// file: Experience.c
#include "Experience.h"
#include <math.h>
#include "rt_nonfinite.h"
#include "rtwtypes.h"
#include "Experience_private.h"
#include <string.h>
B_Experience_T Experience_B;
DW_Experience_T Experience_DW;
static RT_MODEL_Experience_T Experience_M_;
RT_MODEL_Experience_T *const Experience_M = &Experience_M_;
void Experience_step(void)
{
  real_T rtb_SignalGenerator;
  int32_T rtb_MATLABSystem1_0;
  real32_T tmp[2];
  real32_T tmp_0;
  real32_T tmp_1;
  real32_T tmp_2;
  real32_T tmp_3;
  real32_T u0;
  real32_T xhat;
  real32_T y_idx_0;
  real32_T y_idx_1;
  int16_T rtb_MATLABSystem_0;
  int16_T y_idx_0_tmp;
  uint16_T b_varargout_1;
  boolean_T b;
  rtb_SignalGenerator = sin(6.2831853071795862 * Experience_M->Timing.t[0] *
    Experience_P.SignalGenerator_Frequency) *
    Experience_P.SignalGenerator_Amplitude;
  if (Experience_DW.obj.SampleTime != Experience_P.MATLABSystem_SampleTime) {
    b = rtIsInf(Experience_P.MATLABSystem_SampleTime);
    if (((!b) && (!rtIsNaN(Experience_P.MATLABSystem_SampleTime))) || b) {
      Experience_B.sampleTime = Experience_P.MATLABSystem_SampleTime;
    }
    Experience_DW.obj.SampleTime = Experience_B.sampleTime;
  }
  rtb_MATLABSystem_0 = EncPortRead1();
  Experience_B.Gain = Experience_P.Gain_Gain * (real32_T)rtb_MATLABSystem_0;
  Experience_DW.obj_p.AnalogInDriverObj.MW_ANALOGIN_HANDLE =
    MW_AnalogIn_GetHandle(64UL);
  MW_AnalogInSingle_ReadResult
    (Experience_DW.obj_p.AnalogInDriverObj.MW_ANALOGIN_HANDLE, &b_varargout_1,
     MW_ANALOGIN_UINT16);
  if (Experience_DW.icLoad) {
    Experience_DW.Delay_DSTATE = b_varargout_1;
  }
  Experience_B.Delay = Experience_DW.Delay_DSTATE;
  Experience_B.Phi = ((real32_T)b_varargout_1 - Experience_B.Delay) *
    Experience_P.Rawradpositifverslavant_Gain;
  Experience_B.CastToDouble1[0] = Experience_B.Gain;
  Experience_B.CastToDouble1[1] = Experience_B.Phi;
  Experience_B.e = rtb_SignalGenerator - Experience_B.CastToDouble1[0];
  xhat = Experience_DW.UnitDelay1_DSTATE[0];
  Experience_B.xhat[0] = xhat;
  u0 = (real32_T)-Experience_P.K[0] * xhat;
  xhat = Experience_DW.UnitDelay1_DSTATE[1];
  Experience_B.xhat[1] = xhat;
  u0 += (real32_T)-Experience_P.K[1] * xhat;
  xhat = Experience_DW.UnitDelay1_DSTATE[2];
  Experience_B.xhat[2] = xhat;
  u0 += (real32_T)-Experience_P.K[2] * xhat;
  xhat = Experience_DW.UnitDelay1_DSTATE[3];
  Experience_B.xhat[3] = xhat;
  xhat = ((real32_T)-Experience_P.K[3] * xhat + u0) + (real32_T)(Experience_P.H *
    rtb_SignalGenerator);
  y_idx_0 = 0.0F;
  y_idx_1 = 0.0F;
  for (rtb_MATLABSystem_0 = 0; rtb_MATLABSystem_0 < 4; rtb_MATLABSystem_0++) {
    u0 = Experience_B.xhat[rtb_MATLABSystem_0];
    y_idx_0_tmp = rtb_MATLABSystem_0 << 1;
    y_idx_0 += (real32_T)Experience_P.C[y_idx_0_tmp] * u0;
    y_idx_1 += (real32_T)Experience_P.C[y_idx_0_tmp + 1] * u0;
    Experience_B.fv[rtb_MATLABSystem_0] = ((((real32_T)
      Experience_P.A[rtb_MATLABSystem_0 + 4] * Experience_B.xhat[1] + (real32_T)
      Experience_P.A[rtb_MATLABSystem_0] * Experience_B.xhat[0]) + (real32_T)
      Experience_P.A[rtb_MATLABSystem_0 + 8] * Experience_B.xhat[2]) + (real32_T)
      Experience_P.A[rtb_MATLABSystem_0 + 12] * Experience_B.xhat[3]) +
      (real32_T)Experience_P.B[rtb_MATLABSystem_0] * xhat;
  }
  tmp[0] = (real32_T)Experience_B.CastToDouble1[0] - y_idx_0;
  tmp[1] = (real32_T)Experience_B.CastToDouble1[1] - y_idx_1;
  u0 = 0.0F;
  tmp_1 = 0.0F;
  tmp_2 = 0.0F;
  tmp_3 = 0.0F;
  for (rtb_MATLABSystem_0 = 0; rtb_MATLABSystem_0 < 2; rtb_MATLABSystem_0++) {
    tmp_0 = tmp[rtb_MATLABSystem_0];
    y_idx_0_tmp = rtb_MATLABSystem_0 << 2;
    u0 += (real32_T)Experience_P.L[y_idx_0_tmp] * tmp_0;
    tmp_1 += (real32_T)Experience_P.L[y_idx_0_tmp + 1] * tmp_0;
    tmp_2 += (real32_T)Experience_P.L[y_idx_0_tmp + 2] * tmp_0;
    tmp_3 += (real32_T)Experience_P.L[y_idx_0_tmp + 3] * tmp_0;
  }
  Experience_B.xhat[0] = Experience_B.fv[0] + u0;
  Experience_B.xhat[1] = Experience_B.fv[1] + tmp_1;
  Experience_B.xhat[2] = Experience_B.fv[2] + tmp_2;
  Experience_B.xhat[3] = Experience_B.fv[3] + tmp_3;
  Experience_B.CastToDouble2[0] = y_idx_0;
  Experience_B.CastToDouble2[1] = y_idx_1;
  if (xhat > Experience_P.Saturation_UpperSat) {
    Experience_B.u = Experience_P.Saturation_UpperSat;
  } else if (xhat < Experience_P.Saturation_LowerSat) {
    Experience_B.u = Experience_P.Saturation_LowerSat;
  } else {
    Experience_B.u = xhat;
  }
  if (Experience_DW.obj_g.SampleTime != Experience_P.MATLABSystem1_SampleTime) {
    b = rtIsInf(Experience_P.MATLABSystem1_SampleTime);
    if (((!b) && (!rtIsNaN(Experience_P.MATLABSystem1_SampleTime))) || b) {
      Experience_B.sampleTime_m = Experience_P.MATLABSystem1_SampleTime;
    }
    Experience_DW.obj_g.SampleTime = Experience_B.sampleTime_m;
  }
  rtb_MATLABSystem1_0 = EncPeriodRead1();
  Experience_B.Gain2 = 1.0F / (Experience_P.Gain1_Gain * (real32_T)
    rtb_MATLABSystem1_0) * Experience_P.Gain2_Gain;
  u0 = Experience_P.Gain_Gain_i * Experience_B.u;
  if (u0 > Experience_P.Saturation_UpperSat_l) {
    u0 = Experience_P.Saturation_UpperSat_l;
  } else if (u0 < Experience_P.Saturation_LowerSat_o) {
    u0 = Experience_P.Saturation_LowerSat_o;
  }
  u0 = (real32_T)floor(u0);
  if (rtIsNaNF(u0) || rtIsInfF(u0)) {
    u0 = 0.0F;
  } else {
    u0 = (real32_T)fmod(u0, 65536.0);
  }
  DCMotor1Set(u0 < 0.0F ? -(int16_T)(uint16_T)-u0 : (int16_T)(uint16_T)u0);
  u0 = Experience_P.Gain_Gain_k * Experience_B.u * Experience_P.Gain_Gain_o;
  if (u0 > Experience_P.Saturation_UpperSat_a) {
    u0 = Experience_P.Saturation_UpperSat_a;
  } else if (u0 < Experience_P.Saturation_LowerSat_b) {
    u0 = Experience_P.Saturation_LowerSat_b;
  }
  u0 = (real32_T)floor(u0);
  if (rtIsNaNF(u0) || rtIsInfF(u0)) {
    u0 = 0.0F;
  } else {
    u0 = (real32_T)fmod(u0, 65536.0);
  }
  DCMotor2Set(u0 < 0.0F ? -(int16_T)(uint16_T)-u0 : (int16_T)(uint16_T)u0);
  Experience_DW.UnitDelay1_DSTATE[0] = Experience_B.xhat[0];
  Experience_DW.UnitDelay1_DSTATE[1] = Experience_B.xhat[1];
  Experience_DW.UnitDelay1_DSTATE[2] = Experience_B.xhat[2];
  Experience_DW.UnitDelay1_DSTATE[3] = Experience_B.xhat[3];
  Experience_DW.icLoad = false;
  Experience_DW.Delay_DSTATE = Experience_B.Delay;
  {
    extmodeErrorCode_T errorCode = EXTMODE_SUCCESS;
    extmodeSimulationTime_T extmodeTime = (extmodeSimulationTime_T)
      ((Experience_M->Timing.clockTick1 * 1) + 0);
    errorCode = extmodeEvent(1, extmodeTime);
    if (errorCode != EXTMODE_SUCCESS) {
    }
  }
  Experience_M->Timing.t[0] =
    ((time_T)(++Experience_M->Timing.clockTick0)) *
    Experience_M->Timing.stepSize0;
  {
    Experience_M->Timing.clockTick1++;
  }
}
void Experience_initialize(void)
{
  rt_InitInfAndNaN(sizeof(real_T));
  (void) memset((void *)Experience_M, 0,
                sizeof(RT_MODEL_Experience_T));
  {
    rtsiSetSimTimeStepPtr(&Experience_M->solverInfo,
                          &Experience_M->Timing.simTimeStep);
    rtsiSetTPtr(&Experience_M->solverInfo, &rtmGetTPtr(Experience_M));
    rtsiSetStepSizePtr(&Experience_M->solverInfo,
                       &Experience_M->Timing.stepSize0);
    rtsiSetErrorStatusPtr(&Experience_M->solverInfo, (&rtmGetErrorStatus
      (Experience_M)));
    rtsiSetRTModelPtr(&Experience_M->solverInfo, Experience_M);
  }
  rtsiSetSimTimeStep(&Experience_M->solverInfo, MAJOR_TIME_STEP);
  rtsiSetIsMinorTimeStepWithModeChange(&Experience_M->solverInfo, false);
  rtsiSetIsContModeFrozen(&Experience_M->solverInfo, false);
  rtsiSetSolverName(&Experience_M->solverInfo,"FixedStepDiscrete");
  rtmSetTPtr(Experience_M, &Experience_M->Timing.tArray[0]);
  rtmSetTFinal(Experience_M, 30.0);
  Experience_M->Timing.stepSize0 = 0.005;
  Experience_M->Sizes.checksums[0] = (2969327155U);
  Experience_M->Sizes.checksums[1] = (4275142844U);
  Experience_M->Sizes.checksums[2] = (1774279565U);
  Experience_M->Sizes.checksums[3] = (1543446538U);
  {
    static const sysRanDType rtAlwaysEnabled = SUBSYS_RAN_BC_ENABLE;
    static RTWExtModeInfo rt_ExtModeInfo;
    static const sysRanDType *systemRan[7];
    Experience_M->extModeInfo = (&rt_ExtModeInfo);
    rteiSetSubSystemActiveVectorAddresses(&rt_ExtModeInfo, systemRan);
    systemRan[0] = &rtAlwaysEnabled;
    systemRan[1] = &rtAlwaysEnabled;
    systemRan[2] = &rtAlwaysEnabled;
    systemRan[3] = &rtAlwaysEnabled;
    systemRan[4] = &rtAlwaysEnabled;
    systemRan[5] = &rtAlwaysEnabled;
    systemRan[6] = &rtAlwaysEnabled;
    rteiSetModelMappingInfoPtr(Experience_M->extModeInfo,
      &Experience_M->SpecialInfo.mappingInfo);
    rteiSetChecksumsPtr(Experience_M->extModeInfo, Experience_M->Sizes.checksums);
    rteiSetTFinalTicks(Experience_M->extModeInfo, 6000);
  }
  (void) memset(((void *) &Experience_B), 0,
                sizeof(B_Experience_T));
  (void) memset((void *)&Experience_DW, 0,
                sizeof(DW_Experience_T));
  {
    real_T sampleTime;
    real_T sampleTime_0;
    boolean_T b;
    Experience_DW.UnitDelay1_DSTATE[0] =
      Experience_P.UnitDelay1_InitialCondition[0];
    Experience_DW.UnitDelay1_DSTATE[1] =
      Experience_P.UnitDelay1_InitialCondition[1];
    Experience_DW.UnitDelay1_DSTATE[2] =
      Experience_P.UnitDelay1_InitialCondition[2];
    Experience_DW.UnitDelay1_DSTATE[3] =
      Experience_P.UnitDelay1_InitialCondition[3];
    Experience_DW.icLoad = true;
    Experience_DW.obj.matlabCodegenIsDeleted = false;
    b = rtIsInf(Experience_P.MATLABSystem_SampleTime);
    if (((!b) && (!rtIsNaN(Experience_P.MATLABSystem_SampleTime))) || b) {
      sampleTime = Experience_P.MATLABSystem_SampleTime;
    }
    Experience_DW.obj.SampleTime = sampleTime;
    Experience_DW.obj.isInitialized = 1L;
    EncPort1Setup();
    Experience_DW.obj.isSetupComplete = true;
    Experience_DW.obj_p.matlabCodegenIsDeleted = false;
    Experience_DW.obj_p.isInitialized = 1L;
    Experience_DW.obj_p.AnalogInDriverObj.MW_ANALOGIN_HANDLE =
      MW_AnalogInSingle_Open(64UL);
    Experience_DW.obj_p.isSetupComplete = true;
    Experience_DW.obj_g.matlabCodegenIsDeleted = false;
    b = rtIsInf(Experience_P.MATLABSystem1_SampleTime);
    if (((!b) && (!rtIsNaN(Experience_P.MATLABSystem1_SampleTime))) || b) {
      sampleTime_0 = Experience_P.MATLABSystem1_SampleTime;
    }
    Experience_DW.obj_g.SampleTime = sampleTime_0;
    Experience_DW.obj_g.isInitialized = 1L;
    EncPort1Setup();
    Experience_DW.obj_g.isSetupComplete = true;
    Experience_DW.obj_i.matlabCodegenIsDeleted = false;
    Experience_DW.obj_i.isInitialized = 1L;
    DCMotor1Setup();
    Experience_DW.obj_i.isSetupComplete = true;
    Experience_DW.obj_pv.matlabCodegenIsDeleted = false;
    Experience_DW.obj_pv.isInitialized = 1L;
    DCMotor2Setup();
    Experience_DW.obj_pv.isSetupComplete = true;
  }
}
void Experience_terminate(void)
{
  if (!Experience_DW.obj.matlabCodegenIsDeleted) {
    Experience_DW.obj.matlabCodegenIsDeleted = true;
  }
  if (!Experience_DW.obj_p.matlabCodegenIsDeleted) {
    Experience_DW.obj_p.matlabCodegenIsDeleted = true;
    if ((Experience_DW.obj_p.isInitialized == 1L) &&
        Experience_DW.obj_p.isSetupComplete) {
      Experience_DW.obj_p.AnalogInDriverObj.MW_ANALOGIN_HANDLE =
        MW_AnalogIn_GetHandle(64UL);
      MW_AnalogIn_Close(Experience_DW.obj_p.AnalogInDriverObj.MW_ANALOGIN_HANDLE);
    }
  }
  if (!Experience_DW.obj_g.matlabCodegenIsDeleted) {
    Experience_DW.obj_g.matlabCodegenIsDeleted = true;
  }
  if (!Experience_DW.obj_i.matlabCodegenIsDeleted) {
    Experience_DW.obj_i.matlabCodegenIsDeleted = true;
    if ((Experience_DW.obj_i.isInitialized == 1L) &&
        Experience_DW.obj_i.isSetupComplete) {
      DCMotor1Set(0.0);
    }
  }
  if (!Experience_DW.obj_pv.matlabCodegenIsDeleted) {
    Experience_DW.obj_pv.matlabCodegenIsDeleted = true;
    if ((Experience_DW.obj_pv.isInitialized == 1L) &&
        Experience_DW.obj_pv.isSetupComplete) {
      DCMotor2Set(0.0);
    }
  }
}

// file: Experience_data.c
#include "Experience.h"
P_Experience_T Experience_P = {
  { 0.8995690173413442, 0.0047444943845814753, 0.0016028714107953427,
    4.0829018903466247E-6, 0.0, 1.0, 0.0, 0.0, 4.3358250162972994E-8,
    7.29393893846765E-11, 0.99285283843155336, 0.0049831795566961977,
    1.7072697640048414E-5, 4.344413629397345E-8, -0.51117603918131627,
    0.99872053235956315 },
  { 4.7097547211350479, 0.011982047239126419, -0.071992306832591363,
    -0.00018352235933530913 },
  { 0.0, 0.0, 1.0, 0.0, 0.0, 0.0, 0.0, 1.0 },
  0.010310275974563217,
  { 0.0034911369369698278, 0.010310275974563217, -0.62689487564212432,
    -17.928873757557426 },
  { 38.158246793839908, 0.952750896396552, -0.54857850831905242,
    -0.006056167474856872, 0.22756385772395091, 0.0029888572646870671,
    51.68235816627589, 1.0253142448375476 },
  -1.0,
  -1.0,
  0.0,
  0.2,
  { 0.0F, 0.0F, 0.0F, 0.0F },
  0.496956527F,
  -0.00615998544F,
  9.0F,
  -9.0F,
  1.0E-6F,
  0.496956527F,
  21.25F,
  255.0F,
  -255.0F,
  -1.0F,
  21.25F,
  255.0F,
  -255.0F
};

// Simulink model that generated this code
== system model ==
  MATLABSystem : MATLABSystem  <- 1: DataTypeConversion#1
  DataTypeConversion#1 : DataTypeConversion  <- 1: Saturation
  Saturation : Saturate  UpperLimit=255  LowerLimit=-255  <- 1: Gain
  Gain : Gain  Gain=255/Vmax  <- 1: Gain#1
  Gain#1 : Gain  Gain=-1  <- 1: Saturate#1
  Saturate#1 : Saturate  UpperLimit=9  LowerLimit=-9  <- 1: DataTypeConversion#2
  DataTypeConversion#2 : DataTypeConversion  <- 1: MATLABFunction#1/2
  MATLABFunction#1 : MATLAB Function  <- 1: UnitDelay1, 2: SignalGenerator, 3: CastToDouble1
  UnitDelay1 : UnitDelay  InitialCondition=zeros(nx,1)  <- 1: MATLABFunction#1
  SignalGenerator : SignalGenerator  Amplitude=0  Frequency=.2
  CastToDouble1 : DataTypeConversion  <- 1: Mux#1
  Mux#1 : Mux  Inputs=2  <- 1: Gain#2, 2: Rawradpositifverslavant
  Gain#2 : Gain  Gain=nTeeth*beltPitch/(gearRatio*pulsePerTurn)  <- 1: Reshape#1
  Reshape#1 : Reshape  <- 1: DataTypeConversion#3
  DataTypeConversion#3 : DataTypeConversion  <- 1: MATLABSystem#1
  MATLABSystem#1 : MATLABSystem
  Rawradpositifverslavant : Gain  Gain=-pi/2/255  <- 1: Sum#1
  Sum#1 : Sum  Inputs=+-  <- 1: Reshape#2, 2: Delay
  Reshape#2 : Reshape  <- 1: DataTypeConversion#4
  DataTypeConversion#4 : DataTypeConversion  <- 1: AnalogInput#1
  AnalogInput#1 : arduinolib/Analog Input  pinNumber=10
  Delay : Delay  DelayLength=1  <- 1: Delay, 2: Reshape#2
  CastToDouble2 : DataTypeConversion  <- 1: MATLABFunction#1/3
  MATLABSystem1 : MATLABSystem  <- 1: DataTypeConversion#5
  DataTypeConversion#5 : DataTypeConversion  <- 1: Saturate#2
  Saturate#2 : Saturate  UpperLimit=255  LowerLimit=-255  <- 1: Gain#3
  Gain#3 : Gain  Gain=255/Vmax  <- 1: Saturate#1
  Gain2 : Gain  Gain=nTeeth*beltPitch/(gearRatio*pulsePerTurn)  <- 1: Math#1
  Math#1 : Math  Operator=reciprocal  <- 1: Gain1
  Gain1 : Gain  Gain=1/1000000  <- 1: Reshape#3
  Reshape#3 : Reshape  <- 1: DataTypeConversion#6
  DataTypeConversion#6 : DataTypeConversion  <- 1: MATLABSystem#2
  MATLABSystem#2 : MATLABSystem
== matlab function MATLABFunction#1 ==
function [xhat,u,yhat,e] = ControlFF(xhat,r,y,L, C, B, A, K, H)

z = y(1);
e = r-z;
u = -K*xhat+H*r; 

yhat = C*xhat;
xhat = A*xhat+B*u+L*(y-yhat);
